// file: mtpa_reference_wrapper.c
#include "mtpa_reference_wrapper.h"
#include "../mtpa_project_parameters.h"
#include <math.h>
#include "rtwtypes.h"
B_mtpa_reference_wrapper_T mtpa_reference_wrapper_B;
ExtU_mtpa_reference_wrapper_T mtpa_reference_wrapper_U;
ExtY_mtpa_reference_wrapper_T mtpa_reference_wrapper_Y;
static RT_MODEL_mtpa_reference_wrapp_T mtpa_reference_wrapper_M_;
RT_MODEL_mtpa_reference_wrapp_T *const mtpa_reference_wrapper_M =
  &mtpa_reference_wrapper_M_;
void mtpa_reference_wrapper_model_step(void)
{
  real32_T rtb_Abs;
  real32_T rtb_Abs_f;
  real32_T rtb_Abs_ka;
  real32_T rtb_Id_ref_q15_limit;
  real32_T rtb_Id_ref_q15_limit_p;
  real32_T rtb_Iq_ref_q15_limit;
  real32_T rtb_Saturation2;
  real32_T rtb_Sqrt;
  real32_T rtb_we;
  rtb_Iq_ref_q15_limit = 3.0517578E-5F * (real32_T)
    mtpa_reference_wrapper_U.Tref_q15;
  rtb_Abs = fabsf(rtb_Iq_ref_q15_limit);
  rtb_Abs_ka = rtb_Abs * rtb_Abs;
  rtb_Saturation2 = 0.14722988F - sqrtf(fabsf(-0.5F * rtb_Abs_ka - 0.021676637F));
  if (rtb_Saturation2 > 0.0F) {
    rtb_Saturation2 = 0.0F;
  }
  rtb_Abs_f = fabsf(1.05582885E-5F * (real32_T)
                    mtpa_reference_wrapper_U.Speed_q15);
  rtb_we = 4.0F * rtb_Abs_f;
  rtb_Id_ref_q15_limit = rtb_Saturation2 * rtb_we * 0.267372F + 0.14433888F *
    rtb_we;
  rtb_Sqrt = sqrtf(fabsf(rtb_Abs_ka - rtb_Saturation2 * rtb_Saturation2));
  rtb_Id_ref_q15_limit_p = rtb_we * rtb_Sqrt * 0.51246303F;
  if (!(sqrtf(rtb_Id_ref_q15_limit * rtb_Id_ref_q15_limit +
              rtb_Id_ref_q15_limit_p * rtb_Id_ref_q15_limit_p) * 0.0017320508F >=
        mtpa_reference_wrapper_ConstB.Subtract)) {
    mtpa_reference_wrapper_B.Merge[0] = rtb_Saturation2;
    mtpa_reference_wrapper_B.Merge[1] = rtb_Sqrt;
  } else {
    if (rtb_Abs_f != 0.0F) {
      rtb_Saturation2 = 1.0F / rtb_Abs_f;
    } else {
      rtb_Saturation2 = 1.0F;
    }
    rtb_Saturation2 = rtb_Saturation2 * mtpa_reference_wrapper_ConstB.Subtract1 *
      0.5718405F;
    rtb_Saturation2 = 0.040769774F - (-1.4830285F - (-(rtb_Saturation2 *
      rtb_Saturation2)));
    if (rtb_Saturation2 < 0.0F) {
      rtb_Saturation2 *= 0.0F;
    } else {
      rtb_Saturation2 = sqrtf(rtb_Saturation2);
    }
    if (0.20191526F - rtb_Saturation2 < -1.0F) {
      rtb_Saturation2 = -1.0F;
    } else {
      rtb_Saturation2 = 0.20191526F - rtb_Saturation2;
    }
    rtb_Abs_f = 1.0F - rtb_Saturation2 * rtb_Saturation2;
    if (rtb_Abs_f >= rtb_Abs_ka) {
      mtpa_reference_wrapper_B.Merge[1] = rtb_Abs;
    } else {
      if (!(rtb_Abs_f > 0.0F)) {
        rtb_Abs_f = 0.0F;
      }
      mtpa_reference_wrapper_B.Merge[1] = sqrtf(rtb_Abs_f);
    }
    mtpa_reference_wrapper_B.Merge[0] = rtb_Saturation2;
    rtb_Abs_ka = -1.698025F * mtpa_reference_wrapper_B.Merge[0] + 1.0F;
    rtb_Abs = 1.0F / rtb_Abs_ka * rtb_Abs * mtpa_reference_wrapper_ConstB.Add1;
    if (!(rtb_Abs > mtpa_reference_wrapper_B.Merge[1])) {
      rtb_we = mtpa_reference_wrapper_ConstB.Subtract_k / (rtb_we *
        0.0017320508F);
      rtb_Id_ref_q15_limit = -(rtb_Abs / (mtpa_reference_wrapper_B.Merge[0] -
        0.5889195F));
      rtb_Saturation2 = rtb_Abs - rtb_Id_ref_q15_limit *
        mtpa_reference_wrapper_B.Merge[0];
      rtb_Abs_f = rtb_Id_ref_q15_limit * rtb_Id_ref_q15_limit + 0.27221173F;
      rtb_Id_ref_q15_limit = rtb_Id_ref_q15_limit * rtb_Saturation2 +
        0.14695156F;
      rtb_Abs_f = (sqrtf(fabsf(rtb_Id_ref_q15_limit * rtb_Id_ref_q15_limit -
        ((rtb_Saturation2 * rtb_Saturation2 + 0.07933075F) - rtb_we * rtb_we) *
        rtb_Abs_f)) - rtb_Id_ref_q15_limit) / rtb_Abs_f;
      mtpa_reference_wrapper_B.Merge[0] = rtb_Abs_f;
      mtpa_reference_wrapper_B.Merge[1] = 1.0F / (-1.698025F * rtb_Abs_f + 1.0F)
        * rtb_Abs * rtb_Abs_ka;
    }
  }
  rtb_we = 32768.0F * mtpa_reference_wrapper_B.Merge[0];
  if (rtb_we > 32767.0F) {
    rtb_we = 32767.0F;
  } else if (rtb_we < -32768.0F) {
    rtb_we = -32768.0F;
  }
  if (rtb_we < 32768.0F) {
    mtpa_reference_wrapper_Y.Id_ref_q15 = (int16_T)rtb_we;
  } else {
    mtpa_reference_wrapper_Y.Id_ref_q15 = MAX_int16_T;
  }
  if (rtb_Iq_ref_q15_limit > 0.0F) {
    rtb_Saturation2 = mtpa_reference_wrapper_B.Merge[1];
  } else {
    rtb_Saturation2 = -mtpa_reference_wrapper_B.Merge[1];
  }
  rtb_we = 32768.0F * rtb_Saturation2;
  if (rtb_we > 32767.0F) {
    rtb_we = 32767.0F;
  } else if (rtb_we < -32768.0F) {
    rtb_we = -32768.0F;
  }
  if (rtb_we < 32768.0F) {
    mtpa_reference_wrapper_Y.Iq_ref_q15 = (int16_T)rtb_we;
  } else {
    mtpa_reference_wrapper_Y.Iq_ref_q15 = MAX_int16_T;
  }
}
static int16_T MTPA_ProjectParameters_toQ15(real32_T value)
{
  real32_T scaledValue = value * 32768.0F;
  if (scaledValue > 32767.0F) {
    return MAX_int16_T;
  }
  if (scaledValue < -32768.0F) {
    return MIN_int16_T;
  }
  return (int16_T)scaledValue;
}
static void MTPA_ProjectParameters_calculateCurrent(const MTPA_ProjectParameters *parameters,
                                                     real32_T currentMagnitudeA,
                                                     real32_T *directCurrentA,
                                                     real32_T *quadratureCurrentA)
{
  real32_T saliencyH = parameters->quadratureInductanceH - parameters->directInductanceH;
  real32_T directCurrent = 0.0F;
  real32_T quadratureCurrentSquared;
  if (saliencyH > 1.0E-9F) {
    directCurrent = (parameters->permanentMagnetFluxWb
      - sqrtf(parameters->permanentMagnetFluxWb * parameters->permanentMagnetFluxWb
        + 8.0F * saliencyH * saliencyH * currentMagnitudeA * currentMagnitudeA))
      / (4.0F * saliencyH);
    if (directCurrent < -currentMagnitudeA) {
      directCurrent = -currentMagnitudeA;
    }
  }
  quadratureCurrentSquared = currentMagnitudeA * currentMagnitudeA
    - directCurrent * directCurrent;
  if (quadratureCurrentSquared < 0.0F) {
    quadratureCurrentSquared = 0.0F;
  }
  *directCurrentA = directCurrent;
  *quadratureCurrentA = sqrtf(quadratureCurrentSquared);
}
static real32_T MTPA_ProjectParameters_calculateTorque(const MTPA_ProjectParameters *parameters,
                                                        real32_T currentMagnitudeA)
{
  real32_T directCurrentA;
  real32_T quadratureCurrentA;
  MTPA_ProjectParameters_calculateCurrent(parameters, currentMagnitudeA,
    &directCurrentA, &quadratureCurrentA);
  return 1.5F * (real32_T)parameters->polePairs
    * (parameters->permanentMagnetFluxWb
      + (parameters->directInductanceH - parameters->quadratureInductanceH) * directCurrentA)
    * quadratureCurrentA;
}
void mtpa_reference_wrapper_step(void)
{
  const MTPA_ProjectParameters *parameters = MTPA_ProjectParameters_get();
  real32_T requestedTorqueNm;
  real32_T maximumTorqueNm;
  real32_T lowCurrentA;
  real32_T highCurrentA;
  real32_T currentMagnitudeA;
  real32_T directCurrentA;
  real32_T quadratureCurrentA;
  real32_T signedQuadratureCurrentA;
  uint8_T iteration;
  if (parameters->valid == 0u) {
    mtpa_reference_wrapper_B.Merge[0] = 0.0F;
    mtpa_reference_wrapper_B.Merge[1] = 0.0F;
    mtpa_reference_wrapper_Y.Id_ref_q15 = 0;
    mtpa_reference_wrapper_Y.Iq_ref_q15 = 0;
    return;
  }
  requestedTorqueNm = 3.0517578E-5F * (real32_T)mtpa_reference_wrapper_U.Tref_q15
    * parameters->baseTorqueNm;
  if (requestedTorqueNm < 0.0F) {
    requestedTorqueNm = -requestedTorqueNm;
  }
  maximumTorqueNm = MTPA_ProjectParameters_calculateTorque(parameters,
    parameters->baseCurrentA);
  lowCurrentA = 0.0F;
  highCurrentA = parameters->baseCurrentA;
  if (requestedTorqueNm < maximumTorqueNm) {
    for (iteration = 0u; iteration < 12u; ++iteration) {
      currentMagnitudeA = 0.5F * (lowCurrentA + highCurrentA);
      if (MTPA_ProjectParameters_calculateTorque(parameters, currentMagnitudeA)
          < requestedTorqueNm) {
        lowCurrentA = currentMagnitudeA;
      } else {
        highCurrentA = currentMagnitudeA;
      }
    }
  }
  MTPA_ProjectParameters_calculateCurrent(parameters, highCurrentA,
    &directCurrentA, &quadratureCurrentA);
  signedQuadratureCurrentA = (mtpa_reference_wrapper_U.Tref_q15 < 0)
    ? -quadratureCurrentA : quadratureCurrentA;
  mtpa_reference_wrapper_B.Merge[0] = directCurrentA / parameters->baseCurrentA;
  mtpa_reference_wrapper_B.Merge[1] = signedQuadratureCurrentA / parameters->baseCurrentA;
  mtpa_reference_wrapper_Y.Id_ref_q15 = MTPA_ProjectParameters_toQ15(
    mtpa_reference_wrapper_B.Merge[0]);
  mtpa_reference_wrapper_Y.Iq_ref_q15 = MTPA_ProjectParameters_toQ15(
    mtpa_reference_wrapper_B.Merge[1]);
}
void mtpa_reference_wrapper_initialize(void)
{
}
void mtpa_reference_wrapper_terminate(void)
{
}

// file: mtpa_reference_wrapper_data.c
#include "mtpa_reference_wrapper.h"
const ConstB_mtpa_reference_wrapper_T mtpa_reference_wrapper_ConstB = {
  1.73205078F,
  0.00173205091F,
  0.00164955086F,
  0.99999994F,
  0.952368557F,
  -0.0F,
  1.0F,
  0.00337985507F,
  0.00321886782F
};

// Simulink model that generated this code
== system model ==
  Tref_q15 : Inport
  Speed_q15 : Inport
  Id_ref_q15 : Outport  <- 1: DataTypeConversion#1
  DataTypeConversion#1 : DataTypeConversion  <- 1: Id_ref_q15_limit
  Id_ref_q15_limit : Saturate  UpperLimit=32767.0  LowerLimit=-32768.0  <- 1: Gain#1
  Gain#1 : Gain  Gain=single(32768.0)  <- 1: MTPAControlReference#1
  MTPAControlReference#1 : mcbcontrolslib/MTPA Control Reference  <- 1: Gain#2, 2: Gain#3
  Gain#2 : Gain  Gain=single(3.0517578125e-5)  <- 1: DataTypeConversion#2
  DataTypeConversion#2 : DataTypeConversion  <- 1: Tref_q15
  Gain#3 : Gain  Gain=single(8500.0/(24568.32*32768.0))  <- 1: DataTypeConversion#3
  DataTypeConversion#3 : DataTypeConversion  <- 1: Speed_q15
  Iq_ref_q15 : Outport  <- 1: DataTypeConversion#4
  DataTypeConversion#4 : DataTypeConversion  <- 1: Iq_ref_q15_limit
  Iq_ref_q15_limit : Saturate  UpperLimit=32767.0  LowerLimit=-32768.0  <- 1: Gain#4
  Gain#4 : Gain  Gain=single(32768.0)  <- 1: MTPAControlReference#1/2
